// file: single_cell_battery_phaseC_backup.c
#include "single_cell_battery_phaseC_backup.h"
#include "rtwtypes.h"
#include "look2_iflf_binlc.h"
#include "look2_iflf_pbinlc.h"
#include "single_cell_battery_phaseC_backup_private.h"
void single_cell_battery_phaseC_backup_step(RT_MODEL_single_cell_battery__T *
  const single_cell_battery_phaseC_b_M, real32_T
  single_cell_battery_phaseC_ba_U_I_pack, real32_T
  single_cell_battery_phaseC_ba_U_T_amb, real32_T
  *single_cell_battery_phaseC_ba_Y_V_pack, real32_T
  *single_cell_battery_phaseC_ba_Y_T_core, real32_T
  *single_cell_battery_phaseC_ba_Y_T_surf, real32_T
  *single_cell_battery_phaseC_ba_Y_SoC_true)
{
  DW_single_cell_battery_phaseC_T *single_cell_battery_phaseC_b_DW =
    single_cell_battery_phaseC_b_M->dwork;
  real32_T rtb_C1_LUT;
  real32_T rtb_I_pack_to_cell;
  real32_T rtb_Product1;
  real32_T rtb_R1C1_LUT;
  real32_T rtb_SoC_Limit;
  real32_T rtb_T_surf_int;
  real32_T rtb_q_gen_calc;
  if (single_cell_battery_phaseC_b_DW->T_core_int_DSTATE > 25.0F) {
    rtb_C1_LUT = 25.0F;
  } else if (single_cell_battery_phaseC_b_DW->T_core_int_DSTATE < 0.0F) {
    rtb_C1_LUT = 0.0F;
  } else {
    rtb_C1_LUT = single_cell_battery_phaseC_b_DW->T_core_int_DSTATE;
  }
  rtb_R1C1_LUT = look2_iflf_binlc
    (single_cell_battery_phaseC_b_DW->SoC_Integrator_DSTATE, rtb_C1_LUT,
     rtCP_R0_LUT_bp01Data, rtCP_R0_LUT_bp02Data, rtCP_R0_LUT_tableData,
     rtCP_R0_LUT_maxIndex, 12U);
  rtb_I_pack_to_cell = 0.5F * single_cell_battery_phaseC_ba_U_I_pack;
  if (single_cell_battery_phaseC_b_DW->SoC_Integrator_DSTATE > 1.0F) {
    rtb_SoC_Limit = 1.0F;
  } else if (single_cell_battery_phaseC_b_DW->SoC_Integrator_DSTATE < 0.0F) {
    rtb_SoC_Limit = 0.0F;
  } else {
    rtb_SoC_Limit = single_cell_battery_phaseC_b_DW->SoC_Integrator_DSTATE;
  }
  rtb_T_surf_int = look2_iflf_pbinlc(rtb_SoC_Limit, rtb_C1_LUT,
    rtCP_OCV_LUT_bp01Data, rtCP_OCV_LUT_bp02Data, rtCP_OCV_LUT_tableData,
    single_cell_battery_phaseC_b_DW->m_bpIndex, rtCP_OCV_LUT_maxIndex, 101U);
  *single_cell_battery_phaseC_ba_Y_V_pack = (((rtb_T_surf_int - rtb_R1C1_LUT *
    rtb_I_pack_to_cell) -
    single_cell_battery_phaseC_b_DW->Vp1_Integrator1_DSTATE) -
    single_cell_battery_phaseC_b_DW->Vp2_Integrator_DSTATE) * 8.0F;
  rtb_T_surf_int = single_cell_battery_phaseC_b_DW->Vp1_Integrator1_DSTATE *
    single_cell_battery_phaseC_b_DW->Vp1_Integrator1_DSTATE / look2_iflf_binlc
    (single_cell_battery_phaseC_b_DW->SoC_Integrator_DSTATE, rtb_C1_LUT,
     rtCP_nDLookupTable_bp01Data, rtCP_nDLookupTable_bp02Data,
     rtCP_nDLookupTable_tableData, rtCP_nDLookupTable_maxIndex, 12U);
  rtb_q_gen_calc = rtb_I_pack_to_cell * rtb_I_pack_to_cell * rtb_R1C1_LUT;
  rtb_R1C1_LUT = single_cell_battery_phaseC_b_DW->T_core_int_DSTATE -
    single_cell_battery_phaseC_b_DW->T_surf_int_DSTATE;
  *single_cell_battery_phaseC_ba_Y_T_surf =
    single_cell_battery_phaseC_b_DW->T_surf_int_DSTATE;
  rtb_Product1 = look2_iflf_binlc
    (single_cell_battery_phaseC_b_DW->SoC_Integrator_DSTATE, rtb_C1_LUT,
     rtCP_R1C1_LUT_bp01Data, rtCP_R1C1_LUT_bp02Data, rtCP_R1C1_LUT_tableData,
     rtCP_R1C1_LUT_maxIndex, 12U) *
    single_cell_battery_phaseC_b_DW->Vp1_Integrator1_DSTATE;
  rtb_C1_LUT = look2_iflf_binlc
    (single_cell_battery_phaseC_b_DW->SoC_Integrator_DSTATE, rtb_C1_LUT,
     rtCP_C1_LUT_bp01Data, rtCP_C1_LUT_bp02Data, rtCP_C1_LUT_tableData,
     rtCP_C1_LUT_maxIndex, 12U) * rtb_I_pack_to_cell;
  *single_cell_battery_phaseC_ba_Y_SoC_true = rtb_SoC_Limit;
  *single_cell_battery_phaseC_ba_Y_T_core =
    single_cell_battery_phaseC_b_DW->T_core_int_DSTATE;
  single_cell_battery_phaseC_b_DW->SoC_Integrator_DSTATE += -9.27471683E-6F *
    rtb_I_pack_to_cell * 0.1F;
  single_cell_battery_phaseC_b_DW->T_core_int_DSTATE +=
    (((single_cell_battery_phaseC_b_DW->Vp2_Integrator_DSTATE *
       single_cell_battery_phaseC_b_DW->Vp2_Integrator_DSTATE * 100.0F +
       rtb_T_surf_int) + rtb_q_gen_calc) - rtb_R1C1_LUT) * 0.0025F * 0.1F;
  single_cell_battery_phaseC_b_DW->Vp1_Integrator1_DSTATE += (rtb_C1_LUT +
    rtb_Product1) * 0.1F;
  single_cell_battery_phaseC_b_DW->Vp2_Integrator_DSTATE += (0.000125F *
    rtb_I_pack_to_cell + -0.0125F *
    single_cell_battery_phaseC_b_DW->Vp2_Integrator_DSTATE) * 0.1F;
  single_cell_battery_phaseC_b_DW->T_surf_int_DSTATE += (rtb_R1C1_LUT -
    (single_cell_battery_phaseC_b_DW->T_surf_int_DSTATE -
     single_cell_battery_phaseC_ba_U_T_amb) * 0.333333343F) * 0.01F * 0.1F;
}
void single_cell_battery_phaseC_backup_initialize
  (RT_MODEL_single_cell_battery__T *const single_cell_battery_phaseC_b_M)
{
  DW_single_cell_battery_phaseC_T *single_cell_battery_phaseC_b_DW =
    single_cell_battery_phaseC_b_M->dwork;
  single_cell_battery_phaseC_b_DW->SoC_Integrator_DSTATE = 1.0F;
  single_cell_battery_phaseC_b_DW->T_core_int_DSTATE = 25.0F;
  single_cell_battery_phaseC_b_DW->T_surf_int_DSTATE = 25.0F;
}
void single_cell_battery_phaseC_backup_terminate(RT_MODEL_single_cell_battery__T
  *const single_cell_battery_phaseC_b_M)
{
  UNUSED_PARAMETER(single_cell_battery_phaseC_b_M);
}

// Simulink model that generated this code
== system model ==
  I_pack : Inport
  T_amb : Inport
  V_pack : Outport  <- 1: Gain#1
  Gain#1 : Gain  Gain=8  <- 1: Sum#1
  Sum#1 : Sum  Inputs=+---  <- 1: OCV_LUT, 2: Product#1, 3: Vp1_Integrator1, 4: Vp2_Integrator
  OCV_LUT : Lookup_n-D  BreakpointsForDimension1=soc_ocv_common  BreakpointsForDimension2=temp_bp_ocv  Table=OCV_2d  <- 1: SoC_Limit, 2: Saturate#1
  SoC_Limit : Saturate  UpperLimit=1  LowerLimit=0  <- 1: SoC_Integrator
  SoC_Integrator : DiscreteIntegrator  InitialCondition=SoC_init  <- 1: Gain#2
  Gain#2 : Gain  Gain=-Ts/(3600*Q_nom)  <- 1: I_pack_to_cell
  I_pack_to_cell : Gain  Gain=0.5  <- 1: I_pack
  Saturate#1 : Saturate  UpperLimit=25  LowerLimit=0  <- 1: T_core_int
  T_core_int : DiscreteIntegrator  InitialCondition=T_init  <- 1: Gain#3
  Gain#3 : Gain  Gain=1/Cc  <- 1: Sum#2
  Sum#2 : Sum  Inputs=+-  <- 1: Sum#3, 2: Gain#4
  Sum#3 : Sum  Inputs=+++  <- 1: Product#2, 2: Gain#5, 3: q_gen_calc
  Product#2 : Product  Inputs=*/  <- 1: Product#3, 2: nDLookupTable
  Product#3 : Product  <- 1: Vp1_Integrator1, 2: Vp1_Integrator1
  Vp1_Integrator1 : DiscreteIntegrator  <- 1: Sum#4
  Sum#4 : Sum  <- 1: Product#4, 2: Product1
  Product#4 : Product  <- 1: C1_LUT, 2: I_pack_to_cell
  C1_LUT : Lookup_n-D  BreakpointsForDimension1=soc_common  BreakpointsForDimension2=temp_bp  Table=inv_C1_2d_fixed  <- 1: SoC_Integrator, 2: Saturate#1
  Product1 : Product  <- 1: R1C1_LUT, 2: Vp1_Integrator1
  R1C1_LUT : Lookup_n-D  BreakpointsForDimension1=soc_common  BreakpointsForDimension2=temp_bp  Table=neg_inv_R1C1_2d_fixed  <- 1: SoC_Integrator, 2: Saturate#1
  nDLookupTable : Lookup_n-D  BreakpointsForDimension1=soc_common  BreakpointsForDimension2=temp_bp  Table=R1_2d  <- 1: SoC_Integrator, 2: Saturate#1
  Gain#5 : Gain  Gain=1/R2  <- 1: Product#5
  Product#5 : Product  <- 1: Vp2_Integrator, 2: Vp2_Integrator
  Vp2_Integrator : DiscreteIntegrator  <- 1: Sum#5
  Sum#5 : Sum  <- 1: Gain#6, 2: Gain#7
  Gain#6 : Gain  Gain=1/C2  <- 1: I_pack_to_cell
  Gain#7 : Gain  Gain=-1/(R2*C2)  <- 1: Vp2_Integrator
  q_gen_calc : Product  Inputs=**  <- 1: Product#6, 2: R0_LUT
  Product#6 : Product  Inputs=**  <- 1: I_pack_to_cell, 2: I_pack_to_cell
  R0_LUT : Lookup_n-D  BreakpointsForDimension1=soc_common  BreakpointsForDimension2=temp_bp  Table=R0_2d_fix  <- 1: SoC_Integrator, 2: Saturate#1
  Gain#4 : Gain  Gain=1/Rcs  <- 1: Sum#6
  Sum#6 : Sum  Inputs=+-  <- 1: T_core_int, 2: T_surf_int
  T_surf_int : DiscreteIntegrator  InitialCondition=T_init  <- 1: Gain#8
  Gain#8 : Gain  Gain=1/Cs  <- 1: Sum#7
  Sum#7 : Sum  Inputs=+-  <- 1: Gain#4, 2: Gain#9
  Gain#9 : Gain  Gain=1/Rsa  <- 1: Sum#8
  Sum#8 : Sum  Inputs=+-  <- 1: T_surf_int, 2: T_amb
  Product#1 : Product  <- 1: R0_LUT, 2: I_pack_to_cell
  T_core : Outport  <- 1: T_core_int
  T_surf : Outport  <- 1: T_surf_int
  SoC_true : Outport  <- 1: SoC_Limit
